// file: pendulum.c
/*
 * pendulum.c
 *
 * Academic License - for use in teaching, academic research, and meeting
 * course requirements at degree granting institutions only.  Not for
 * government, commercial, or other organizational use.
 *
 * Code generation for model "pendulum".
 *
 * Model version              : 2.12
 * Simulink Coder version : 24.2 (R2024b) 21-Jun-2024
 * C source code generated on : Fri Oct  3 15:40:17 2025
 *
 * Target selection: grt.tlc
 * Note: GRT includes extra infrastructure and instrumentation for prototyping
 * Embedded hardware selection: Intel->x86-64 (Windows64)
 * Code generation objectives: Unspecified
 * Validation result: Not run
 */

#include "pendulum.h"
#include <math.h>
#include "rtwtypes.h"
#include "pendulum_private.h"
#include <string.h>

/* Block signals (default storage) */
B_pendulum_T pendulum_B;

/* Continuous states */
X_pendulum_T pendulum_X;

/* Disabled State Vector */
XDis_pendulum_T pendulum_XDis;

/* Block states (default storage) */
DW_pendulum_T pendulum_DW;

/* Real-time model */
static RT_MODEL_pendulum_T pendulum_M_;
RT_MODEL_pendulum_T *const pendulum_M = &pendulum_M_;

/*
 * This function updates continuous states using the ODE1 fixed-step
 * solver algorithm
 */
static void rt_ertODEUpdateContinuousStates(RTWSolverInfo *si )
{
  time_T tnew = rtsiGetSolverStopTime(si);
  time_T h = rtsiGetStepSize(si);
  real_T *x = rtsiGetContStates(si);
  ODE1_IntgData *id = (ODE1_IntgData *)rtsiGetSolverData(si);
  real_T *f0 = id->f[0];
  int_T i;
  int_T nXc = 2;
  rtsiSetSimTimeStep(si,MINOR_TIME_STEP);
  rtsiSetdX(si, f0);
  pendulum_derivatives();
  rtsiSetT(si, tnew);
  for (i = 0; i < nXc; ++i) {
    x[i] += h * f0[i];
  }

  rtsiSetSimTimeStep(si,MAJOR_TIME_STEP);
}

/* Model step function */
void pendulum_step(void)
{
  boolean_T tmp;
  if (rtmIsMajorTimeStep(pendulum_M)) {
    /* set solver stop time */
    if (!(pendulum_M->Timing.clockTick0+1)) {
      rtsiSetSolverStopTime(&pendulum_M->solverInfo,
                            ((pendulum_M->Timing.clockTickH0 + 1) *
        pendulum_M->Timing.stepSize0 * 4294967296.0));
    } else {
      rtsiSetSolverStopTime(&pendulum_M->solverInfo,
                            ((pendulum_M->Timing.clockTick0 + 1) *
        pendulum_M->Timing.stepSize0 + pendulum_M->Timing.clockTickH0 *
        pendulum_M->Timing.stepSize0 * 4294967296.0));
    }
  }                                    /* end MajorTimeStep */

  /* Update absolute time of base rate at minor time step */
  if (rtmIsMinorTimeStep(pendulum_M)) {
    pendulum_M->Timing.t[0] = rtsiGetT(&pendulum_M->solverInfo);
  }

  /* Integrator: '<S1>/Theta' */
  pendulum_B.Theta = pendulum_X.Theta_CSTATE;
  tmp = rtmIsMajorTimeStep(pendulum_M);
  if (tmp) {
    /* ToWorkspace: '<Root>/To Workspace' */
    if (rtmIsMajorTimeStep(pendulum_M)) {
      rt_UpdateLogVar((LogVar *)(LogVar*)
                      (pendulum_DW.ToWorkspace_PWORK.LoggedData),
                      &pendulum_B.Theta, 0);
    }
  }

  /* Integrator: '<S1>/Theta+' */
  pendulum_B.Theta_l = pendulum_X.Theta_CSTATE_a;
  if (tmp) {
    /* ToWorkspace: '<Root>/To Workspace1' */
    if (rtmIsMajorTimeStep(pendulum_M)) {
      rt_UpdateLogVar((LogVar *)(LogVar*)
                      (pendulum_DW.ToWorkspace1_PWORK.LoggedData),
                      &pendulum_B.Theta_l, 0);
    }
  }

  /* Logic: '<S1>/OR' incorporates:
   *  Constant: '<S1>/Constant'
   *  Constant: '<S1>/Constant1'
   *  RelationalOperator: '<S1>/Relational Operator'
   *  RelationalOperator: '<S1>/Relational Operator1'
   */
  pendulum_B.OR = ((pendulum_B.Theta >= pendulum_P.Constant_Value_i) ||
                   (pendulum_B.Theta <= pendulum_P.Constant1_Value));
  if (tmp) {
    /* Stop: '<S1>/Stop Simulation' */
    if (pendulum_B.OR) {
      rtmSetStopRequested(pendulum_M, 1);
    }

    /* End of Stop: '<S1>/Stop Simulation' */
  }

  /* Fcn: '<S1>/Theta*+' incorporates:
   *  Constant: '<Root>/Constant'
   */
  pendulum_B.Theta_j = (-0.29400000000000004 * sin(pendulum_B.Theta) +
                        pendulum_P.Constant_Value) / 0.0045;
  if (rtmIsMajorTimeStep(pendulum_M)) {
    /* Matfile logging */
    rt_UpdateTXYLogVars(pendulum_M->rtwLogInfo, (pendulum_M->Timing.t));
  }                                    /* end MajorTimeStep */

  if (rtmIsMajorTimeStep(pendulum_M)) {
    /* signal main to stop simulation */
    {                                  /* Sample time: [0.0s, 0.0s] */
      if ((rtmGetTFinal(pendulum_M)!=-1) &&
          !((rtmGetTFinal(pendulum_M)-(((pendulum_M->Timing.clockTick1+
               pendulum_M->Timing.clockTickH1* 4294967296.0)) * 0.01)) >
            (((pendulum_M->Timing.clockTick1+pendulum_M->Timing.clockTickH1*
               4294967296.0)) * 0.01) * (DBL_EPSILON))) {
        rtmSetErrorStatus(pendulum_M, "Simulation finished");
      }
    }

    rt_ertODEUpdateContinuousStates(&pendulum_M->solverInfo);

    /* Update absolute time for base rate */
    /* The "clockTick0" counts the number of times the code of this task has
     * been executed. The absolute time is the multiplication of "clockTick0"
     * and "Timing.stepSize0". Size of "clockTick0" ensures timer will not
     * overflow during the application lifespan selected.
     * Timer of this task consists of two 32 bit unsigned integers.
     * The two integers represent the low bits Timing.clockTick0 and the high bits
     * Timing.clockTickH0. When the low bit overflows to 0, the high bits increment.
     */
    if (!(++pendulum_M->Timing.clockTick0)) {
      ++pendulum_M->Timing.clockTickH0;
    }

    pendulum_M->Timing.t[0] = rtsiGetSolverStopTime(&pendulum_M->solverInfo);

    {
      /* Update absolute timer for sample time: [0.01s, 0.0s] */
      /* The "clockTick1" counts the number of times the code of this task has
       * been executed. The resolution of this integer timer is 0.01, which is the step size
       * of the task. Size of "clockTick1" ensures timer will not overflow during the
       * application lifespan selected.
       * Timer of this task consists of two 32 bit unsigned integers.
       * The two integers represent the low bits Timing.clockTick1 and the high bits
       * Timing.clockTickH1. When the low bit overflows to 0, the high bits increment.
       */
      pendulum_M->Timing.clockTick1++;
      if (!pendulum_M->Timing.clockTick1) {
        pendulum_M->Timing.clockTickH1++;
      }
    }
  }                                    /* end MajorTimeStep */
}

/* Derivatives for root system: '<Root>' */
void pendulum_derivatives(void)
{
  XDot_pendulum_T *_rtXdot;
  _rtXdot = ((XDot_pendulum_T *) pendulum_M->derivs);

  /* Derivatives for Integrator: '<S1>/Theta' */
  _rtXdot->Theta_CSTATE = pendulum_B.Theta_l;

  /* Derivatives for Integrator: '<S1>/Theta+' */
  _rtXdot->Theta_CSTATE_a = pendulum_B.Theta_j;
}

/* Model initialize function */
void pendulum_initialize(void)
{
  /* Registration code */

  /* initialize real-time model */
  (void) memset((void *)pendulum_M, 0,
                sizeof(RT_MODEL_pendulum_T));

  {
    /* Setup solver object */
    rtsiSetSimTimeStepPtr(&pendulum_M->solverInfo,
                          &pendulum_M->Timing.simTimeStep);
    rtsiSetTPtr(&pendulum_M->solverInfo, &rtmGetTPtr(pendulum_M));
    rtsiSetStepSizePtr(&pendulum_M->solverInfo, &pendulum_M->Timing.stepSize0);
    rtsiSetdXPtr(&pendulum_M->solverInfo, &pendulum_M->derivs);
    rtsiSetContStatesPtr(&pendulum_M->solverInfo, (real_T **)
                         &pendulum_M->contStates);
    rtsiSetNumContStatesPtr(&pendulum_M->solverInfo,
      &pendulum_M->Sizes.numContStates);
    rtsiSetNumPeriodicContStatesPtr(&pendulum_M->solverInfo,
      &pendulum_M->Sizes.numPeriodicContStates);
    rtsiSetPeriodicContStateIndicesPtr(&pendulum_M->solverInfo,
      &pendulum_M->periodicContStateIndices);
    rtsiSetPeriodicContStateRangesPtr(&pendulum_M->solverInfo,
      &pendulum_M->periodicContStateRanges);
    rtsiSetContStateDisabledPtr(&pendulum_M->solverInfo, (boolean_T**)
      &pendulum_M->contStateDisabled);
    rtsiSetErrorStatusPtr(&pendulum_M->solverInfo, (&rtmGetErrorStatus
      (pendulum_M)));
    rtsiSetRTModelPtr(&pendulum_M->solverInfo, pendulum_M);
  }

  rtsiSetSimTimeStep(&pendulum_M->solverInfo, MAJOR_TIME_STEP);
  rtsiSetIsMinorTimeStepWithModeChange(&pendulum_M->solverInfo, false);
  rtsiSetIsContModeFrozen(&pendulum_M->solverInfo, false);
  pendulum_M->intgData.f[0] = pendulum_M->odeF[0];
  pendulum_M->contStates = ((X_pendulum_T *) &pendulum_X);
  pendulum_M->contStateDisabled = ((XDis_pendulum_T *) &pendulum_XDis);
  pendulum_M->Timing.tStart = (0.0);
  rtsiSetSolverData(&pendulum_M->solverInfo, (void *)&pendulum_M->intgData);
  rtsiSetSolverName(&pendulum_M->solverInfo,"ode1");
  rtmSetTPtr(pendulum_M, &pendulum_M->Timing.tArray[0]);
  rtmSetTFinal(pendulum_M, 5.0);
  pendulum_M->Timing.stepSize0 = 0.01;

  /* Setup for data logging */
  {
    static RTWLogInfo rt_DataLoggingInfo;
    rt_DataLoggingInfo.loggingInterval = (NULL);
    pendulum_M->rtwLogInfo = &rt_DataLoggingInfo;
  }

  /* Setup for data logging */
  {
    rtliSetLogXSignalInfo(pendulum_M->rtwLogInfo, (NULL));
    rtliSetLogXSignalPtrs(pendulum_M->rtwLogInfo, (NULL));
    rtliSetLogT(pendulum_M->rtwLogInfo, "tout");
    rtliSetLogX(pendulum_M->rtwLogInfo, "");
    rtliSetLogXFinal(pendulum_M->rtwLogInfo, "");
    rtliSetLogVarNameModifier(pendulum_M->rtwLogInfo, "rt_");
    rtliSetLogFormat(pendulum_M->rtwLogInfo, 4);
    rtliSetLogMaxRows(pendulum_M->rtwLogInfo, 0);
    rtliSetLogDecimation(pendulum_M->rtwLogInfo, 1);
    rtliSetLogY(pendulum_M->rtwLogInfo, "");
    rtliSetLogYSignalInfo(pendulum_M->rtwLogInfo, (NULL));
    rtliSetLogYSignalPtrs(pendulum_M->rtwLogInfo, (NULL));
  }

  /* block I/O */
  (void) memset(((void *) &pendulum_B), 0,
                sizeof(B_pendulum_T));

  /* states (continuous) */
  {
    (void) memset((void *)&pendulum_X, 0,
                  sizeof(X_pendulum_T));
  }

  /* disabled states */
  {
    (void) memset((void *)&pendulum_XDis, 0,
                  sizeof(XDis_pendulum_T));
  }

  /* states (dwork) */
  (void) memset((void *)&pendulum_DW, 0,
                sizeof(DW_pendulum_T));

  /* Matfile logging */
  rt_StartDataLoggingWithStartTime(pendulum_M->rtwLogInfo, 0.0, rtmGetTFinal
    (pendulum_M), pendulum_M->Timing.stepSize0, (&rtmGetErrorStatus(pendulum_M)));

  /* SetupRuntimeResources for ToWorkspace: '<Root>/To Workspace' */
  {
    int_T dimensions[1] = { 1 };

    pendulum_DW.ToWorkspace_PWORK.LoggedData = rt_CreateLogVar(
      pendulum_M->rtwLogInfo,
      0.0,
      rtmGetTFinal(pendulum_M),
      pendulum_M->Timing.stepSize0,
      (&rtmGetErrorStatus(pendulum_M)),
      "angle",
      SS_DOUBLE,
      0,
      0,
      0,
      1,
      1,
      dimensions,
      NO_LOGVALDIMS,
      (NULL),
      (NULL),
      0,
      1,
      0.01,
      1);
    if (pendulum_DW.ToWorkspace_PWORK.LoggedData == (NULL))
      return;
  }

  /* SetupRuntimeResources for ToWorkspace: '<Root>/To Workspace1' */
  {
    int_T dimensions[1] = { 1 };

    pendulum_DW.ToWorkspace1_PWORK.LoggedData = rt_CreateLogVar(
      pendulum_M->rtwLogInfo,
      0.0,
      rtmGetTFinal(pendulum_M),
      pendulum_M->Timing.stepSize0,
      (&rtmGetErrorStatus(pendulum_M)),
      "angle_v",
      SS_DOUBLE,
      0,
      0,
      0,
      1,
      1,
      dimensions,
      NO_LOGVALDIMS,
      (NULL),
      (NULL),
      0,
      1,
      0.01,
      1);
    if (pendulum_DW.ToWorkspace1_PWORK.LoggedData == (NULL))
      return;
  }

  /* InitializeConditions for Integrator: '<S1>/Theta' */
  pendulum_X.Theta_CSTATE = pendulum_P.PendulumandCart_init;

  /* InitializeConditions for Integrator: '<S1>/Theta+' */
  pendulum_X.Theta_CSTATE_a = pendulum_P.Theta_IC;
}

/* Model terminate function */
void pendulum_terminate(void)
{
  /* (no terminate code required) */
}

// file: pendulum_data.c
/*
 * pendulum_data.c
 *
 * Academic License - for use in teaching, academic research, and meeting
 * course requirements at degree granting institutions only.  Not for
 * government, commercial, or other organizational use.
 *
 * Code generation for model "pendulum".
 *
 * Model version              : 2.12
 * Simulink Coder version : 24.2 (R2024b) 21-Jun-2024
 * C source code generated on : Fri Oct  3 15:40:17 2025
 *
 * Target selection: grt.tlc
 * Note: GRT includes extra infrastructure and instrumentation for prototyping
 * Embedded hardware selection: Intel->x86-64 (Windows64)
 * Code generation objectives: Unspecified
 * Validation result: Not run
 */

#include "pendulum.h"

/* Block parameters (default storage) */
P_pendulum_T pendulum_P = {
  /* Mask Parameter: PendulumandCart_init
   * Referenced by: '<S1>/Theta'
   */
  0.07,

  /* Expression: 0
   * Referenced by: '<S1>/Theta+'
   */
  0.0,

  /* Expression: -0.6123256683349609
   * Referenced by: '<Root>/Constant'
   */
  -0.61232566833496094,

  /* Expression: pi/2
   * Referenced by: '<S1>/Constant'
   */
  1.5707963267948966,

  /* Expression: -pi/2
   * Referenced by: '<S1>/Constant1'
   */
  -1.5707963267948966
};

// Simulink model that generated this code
simulink model "pendulum"  (R2024b)
settings: Solver=ode1  StartTime=0.0  StopTime=5  FixedStep=0.01  MaxStep=0.001  RelTol=1e-3

== system pendulum ==
  note: Inverted Pendulum
  Constant : Constant  Value=-0.6123256683349609
  Pendulum and Cart : Subsystem  mask{m=0.2, l=0.3/2, g=9.8, init=0.07}
      mask prompts: m "Pend Mass (kg):"; l "COM Distance (m):"; g "Acc due to Gravity (g):"; init "Initial Angle (rad):"
  To Workspace : ToWorkspace  VariableName=angle  SampleTime=-1
  To Workspace1 : ToWorkspace  VariableName=angle_v  SampleTime=-1
  wires:
  Pendulum and Cart/1(AngleOut) -> To Workspace/1
  Pendulum and Cart/2(AngularVelocityOut) -> To Workspace1/1
  Constant/1 -> Pendulum and Cart/1(Force)

== system pendulum/Pendulum and Cart ==
  Force : Inport
  Constant : Constant  Value=pi/2
  Constant1 : Constant  Value=-pi/2
  Mux : Mux  Inputs=3
  OR : Logic  Operator=OR  IconShape=distinctive  AllPortsSameDT=off  OutDataTypeStr=boolean
  Relational Operator : RelationalOperator  OutDataTypeStr=boolean  RndMeth=Simplest  InputSameDT=off
  Relational Operator1 : RelationalOperator  Operator=<=  OutDataTypeStr=boolean  RndMeth=Simplest  InputSameDT=off
  Stop Simulation : Stop
  Theta : Integrator  InitialCondition=init
  Theta* : Integrator
  Theta** : Fcn  Expr=(-m*g*l*sin(u(3)) + u(1)) / (m*l^2)
  AngleOut : Outport
  AngularVelocityOut : Outport  Port=2
  wires:
  Mux/1 -> Theta**/1
  Force/1 -> Mux/1
  Theta**/1 -> Theta*/1
  Theta/1 -> AngleOut/1, Relational Operator1/1, Mux/3, Relational Operator/1
  Theta*/1 -> Mux/2, AngularVelocityOut/1, Theta/1
  Constant/1 -> Relational Operator/2
  OR/1 -> Stop Simulation/1
  Relational Operator1/1 -> OR/2
  Constant1/1 -> Relational Operator1/2
  Relational Operator/1 -> OR/1
